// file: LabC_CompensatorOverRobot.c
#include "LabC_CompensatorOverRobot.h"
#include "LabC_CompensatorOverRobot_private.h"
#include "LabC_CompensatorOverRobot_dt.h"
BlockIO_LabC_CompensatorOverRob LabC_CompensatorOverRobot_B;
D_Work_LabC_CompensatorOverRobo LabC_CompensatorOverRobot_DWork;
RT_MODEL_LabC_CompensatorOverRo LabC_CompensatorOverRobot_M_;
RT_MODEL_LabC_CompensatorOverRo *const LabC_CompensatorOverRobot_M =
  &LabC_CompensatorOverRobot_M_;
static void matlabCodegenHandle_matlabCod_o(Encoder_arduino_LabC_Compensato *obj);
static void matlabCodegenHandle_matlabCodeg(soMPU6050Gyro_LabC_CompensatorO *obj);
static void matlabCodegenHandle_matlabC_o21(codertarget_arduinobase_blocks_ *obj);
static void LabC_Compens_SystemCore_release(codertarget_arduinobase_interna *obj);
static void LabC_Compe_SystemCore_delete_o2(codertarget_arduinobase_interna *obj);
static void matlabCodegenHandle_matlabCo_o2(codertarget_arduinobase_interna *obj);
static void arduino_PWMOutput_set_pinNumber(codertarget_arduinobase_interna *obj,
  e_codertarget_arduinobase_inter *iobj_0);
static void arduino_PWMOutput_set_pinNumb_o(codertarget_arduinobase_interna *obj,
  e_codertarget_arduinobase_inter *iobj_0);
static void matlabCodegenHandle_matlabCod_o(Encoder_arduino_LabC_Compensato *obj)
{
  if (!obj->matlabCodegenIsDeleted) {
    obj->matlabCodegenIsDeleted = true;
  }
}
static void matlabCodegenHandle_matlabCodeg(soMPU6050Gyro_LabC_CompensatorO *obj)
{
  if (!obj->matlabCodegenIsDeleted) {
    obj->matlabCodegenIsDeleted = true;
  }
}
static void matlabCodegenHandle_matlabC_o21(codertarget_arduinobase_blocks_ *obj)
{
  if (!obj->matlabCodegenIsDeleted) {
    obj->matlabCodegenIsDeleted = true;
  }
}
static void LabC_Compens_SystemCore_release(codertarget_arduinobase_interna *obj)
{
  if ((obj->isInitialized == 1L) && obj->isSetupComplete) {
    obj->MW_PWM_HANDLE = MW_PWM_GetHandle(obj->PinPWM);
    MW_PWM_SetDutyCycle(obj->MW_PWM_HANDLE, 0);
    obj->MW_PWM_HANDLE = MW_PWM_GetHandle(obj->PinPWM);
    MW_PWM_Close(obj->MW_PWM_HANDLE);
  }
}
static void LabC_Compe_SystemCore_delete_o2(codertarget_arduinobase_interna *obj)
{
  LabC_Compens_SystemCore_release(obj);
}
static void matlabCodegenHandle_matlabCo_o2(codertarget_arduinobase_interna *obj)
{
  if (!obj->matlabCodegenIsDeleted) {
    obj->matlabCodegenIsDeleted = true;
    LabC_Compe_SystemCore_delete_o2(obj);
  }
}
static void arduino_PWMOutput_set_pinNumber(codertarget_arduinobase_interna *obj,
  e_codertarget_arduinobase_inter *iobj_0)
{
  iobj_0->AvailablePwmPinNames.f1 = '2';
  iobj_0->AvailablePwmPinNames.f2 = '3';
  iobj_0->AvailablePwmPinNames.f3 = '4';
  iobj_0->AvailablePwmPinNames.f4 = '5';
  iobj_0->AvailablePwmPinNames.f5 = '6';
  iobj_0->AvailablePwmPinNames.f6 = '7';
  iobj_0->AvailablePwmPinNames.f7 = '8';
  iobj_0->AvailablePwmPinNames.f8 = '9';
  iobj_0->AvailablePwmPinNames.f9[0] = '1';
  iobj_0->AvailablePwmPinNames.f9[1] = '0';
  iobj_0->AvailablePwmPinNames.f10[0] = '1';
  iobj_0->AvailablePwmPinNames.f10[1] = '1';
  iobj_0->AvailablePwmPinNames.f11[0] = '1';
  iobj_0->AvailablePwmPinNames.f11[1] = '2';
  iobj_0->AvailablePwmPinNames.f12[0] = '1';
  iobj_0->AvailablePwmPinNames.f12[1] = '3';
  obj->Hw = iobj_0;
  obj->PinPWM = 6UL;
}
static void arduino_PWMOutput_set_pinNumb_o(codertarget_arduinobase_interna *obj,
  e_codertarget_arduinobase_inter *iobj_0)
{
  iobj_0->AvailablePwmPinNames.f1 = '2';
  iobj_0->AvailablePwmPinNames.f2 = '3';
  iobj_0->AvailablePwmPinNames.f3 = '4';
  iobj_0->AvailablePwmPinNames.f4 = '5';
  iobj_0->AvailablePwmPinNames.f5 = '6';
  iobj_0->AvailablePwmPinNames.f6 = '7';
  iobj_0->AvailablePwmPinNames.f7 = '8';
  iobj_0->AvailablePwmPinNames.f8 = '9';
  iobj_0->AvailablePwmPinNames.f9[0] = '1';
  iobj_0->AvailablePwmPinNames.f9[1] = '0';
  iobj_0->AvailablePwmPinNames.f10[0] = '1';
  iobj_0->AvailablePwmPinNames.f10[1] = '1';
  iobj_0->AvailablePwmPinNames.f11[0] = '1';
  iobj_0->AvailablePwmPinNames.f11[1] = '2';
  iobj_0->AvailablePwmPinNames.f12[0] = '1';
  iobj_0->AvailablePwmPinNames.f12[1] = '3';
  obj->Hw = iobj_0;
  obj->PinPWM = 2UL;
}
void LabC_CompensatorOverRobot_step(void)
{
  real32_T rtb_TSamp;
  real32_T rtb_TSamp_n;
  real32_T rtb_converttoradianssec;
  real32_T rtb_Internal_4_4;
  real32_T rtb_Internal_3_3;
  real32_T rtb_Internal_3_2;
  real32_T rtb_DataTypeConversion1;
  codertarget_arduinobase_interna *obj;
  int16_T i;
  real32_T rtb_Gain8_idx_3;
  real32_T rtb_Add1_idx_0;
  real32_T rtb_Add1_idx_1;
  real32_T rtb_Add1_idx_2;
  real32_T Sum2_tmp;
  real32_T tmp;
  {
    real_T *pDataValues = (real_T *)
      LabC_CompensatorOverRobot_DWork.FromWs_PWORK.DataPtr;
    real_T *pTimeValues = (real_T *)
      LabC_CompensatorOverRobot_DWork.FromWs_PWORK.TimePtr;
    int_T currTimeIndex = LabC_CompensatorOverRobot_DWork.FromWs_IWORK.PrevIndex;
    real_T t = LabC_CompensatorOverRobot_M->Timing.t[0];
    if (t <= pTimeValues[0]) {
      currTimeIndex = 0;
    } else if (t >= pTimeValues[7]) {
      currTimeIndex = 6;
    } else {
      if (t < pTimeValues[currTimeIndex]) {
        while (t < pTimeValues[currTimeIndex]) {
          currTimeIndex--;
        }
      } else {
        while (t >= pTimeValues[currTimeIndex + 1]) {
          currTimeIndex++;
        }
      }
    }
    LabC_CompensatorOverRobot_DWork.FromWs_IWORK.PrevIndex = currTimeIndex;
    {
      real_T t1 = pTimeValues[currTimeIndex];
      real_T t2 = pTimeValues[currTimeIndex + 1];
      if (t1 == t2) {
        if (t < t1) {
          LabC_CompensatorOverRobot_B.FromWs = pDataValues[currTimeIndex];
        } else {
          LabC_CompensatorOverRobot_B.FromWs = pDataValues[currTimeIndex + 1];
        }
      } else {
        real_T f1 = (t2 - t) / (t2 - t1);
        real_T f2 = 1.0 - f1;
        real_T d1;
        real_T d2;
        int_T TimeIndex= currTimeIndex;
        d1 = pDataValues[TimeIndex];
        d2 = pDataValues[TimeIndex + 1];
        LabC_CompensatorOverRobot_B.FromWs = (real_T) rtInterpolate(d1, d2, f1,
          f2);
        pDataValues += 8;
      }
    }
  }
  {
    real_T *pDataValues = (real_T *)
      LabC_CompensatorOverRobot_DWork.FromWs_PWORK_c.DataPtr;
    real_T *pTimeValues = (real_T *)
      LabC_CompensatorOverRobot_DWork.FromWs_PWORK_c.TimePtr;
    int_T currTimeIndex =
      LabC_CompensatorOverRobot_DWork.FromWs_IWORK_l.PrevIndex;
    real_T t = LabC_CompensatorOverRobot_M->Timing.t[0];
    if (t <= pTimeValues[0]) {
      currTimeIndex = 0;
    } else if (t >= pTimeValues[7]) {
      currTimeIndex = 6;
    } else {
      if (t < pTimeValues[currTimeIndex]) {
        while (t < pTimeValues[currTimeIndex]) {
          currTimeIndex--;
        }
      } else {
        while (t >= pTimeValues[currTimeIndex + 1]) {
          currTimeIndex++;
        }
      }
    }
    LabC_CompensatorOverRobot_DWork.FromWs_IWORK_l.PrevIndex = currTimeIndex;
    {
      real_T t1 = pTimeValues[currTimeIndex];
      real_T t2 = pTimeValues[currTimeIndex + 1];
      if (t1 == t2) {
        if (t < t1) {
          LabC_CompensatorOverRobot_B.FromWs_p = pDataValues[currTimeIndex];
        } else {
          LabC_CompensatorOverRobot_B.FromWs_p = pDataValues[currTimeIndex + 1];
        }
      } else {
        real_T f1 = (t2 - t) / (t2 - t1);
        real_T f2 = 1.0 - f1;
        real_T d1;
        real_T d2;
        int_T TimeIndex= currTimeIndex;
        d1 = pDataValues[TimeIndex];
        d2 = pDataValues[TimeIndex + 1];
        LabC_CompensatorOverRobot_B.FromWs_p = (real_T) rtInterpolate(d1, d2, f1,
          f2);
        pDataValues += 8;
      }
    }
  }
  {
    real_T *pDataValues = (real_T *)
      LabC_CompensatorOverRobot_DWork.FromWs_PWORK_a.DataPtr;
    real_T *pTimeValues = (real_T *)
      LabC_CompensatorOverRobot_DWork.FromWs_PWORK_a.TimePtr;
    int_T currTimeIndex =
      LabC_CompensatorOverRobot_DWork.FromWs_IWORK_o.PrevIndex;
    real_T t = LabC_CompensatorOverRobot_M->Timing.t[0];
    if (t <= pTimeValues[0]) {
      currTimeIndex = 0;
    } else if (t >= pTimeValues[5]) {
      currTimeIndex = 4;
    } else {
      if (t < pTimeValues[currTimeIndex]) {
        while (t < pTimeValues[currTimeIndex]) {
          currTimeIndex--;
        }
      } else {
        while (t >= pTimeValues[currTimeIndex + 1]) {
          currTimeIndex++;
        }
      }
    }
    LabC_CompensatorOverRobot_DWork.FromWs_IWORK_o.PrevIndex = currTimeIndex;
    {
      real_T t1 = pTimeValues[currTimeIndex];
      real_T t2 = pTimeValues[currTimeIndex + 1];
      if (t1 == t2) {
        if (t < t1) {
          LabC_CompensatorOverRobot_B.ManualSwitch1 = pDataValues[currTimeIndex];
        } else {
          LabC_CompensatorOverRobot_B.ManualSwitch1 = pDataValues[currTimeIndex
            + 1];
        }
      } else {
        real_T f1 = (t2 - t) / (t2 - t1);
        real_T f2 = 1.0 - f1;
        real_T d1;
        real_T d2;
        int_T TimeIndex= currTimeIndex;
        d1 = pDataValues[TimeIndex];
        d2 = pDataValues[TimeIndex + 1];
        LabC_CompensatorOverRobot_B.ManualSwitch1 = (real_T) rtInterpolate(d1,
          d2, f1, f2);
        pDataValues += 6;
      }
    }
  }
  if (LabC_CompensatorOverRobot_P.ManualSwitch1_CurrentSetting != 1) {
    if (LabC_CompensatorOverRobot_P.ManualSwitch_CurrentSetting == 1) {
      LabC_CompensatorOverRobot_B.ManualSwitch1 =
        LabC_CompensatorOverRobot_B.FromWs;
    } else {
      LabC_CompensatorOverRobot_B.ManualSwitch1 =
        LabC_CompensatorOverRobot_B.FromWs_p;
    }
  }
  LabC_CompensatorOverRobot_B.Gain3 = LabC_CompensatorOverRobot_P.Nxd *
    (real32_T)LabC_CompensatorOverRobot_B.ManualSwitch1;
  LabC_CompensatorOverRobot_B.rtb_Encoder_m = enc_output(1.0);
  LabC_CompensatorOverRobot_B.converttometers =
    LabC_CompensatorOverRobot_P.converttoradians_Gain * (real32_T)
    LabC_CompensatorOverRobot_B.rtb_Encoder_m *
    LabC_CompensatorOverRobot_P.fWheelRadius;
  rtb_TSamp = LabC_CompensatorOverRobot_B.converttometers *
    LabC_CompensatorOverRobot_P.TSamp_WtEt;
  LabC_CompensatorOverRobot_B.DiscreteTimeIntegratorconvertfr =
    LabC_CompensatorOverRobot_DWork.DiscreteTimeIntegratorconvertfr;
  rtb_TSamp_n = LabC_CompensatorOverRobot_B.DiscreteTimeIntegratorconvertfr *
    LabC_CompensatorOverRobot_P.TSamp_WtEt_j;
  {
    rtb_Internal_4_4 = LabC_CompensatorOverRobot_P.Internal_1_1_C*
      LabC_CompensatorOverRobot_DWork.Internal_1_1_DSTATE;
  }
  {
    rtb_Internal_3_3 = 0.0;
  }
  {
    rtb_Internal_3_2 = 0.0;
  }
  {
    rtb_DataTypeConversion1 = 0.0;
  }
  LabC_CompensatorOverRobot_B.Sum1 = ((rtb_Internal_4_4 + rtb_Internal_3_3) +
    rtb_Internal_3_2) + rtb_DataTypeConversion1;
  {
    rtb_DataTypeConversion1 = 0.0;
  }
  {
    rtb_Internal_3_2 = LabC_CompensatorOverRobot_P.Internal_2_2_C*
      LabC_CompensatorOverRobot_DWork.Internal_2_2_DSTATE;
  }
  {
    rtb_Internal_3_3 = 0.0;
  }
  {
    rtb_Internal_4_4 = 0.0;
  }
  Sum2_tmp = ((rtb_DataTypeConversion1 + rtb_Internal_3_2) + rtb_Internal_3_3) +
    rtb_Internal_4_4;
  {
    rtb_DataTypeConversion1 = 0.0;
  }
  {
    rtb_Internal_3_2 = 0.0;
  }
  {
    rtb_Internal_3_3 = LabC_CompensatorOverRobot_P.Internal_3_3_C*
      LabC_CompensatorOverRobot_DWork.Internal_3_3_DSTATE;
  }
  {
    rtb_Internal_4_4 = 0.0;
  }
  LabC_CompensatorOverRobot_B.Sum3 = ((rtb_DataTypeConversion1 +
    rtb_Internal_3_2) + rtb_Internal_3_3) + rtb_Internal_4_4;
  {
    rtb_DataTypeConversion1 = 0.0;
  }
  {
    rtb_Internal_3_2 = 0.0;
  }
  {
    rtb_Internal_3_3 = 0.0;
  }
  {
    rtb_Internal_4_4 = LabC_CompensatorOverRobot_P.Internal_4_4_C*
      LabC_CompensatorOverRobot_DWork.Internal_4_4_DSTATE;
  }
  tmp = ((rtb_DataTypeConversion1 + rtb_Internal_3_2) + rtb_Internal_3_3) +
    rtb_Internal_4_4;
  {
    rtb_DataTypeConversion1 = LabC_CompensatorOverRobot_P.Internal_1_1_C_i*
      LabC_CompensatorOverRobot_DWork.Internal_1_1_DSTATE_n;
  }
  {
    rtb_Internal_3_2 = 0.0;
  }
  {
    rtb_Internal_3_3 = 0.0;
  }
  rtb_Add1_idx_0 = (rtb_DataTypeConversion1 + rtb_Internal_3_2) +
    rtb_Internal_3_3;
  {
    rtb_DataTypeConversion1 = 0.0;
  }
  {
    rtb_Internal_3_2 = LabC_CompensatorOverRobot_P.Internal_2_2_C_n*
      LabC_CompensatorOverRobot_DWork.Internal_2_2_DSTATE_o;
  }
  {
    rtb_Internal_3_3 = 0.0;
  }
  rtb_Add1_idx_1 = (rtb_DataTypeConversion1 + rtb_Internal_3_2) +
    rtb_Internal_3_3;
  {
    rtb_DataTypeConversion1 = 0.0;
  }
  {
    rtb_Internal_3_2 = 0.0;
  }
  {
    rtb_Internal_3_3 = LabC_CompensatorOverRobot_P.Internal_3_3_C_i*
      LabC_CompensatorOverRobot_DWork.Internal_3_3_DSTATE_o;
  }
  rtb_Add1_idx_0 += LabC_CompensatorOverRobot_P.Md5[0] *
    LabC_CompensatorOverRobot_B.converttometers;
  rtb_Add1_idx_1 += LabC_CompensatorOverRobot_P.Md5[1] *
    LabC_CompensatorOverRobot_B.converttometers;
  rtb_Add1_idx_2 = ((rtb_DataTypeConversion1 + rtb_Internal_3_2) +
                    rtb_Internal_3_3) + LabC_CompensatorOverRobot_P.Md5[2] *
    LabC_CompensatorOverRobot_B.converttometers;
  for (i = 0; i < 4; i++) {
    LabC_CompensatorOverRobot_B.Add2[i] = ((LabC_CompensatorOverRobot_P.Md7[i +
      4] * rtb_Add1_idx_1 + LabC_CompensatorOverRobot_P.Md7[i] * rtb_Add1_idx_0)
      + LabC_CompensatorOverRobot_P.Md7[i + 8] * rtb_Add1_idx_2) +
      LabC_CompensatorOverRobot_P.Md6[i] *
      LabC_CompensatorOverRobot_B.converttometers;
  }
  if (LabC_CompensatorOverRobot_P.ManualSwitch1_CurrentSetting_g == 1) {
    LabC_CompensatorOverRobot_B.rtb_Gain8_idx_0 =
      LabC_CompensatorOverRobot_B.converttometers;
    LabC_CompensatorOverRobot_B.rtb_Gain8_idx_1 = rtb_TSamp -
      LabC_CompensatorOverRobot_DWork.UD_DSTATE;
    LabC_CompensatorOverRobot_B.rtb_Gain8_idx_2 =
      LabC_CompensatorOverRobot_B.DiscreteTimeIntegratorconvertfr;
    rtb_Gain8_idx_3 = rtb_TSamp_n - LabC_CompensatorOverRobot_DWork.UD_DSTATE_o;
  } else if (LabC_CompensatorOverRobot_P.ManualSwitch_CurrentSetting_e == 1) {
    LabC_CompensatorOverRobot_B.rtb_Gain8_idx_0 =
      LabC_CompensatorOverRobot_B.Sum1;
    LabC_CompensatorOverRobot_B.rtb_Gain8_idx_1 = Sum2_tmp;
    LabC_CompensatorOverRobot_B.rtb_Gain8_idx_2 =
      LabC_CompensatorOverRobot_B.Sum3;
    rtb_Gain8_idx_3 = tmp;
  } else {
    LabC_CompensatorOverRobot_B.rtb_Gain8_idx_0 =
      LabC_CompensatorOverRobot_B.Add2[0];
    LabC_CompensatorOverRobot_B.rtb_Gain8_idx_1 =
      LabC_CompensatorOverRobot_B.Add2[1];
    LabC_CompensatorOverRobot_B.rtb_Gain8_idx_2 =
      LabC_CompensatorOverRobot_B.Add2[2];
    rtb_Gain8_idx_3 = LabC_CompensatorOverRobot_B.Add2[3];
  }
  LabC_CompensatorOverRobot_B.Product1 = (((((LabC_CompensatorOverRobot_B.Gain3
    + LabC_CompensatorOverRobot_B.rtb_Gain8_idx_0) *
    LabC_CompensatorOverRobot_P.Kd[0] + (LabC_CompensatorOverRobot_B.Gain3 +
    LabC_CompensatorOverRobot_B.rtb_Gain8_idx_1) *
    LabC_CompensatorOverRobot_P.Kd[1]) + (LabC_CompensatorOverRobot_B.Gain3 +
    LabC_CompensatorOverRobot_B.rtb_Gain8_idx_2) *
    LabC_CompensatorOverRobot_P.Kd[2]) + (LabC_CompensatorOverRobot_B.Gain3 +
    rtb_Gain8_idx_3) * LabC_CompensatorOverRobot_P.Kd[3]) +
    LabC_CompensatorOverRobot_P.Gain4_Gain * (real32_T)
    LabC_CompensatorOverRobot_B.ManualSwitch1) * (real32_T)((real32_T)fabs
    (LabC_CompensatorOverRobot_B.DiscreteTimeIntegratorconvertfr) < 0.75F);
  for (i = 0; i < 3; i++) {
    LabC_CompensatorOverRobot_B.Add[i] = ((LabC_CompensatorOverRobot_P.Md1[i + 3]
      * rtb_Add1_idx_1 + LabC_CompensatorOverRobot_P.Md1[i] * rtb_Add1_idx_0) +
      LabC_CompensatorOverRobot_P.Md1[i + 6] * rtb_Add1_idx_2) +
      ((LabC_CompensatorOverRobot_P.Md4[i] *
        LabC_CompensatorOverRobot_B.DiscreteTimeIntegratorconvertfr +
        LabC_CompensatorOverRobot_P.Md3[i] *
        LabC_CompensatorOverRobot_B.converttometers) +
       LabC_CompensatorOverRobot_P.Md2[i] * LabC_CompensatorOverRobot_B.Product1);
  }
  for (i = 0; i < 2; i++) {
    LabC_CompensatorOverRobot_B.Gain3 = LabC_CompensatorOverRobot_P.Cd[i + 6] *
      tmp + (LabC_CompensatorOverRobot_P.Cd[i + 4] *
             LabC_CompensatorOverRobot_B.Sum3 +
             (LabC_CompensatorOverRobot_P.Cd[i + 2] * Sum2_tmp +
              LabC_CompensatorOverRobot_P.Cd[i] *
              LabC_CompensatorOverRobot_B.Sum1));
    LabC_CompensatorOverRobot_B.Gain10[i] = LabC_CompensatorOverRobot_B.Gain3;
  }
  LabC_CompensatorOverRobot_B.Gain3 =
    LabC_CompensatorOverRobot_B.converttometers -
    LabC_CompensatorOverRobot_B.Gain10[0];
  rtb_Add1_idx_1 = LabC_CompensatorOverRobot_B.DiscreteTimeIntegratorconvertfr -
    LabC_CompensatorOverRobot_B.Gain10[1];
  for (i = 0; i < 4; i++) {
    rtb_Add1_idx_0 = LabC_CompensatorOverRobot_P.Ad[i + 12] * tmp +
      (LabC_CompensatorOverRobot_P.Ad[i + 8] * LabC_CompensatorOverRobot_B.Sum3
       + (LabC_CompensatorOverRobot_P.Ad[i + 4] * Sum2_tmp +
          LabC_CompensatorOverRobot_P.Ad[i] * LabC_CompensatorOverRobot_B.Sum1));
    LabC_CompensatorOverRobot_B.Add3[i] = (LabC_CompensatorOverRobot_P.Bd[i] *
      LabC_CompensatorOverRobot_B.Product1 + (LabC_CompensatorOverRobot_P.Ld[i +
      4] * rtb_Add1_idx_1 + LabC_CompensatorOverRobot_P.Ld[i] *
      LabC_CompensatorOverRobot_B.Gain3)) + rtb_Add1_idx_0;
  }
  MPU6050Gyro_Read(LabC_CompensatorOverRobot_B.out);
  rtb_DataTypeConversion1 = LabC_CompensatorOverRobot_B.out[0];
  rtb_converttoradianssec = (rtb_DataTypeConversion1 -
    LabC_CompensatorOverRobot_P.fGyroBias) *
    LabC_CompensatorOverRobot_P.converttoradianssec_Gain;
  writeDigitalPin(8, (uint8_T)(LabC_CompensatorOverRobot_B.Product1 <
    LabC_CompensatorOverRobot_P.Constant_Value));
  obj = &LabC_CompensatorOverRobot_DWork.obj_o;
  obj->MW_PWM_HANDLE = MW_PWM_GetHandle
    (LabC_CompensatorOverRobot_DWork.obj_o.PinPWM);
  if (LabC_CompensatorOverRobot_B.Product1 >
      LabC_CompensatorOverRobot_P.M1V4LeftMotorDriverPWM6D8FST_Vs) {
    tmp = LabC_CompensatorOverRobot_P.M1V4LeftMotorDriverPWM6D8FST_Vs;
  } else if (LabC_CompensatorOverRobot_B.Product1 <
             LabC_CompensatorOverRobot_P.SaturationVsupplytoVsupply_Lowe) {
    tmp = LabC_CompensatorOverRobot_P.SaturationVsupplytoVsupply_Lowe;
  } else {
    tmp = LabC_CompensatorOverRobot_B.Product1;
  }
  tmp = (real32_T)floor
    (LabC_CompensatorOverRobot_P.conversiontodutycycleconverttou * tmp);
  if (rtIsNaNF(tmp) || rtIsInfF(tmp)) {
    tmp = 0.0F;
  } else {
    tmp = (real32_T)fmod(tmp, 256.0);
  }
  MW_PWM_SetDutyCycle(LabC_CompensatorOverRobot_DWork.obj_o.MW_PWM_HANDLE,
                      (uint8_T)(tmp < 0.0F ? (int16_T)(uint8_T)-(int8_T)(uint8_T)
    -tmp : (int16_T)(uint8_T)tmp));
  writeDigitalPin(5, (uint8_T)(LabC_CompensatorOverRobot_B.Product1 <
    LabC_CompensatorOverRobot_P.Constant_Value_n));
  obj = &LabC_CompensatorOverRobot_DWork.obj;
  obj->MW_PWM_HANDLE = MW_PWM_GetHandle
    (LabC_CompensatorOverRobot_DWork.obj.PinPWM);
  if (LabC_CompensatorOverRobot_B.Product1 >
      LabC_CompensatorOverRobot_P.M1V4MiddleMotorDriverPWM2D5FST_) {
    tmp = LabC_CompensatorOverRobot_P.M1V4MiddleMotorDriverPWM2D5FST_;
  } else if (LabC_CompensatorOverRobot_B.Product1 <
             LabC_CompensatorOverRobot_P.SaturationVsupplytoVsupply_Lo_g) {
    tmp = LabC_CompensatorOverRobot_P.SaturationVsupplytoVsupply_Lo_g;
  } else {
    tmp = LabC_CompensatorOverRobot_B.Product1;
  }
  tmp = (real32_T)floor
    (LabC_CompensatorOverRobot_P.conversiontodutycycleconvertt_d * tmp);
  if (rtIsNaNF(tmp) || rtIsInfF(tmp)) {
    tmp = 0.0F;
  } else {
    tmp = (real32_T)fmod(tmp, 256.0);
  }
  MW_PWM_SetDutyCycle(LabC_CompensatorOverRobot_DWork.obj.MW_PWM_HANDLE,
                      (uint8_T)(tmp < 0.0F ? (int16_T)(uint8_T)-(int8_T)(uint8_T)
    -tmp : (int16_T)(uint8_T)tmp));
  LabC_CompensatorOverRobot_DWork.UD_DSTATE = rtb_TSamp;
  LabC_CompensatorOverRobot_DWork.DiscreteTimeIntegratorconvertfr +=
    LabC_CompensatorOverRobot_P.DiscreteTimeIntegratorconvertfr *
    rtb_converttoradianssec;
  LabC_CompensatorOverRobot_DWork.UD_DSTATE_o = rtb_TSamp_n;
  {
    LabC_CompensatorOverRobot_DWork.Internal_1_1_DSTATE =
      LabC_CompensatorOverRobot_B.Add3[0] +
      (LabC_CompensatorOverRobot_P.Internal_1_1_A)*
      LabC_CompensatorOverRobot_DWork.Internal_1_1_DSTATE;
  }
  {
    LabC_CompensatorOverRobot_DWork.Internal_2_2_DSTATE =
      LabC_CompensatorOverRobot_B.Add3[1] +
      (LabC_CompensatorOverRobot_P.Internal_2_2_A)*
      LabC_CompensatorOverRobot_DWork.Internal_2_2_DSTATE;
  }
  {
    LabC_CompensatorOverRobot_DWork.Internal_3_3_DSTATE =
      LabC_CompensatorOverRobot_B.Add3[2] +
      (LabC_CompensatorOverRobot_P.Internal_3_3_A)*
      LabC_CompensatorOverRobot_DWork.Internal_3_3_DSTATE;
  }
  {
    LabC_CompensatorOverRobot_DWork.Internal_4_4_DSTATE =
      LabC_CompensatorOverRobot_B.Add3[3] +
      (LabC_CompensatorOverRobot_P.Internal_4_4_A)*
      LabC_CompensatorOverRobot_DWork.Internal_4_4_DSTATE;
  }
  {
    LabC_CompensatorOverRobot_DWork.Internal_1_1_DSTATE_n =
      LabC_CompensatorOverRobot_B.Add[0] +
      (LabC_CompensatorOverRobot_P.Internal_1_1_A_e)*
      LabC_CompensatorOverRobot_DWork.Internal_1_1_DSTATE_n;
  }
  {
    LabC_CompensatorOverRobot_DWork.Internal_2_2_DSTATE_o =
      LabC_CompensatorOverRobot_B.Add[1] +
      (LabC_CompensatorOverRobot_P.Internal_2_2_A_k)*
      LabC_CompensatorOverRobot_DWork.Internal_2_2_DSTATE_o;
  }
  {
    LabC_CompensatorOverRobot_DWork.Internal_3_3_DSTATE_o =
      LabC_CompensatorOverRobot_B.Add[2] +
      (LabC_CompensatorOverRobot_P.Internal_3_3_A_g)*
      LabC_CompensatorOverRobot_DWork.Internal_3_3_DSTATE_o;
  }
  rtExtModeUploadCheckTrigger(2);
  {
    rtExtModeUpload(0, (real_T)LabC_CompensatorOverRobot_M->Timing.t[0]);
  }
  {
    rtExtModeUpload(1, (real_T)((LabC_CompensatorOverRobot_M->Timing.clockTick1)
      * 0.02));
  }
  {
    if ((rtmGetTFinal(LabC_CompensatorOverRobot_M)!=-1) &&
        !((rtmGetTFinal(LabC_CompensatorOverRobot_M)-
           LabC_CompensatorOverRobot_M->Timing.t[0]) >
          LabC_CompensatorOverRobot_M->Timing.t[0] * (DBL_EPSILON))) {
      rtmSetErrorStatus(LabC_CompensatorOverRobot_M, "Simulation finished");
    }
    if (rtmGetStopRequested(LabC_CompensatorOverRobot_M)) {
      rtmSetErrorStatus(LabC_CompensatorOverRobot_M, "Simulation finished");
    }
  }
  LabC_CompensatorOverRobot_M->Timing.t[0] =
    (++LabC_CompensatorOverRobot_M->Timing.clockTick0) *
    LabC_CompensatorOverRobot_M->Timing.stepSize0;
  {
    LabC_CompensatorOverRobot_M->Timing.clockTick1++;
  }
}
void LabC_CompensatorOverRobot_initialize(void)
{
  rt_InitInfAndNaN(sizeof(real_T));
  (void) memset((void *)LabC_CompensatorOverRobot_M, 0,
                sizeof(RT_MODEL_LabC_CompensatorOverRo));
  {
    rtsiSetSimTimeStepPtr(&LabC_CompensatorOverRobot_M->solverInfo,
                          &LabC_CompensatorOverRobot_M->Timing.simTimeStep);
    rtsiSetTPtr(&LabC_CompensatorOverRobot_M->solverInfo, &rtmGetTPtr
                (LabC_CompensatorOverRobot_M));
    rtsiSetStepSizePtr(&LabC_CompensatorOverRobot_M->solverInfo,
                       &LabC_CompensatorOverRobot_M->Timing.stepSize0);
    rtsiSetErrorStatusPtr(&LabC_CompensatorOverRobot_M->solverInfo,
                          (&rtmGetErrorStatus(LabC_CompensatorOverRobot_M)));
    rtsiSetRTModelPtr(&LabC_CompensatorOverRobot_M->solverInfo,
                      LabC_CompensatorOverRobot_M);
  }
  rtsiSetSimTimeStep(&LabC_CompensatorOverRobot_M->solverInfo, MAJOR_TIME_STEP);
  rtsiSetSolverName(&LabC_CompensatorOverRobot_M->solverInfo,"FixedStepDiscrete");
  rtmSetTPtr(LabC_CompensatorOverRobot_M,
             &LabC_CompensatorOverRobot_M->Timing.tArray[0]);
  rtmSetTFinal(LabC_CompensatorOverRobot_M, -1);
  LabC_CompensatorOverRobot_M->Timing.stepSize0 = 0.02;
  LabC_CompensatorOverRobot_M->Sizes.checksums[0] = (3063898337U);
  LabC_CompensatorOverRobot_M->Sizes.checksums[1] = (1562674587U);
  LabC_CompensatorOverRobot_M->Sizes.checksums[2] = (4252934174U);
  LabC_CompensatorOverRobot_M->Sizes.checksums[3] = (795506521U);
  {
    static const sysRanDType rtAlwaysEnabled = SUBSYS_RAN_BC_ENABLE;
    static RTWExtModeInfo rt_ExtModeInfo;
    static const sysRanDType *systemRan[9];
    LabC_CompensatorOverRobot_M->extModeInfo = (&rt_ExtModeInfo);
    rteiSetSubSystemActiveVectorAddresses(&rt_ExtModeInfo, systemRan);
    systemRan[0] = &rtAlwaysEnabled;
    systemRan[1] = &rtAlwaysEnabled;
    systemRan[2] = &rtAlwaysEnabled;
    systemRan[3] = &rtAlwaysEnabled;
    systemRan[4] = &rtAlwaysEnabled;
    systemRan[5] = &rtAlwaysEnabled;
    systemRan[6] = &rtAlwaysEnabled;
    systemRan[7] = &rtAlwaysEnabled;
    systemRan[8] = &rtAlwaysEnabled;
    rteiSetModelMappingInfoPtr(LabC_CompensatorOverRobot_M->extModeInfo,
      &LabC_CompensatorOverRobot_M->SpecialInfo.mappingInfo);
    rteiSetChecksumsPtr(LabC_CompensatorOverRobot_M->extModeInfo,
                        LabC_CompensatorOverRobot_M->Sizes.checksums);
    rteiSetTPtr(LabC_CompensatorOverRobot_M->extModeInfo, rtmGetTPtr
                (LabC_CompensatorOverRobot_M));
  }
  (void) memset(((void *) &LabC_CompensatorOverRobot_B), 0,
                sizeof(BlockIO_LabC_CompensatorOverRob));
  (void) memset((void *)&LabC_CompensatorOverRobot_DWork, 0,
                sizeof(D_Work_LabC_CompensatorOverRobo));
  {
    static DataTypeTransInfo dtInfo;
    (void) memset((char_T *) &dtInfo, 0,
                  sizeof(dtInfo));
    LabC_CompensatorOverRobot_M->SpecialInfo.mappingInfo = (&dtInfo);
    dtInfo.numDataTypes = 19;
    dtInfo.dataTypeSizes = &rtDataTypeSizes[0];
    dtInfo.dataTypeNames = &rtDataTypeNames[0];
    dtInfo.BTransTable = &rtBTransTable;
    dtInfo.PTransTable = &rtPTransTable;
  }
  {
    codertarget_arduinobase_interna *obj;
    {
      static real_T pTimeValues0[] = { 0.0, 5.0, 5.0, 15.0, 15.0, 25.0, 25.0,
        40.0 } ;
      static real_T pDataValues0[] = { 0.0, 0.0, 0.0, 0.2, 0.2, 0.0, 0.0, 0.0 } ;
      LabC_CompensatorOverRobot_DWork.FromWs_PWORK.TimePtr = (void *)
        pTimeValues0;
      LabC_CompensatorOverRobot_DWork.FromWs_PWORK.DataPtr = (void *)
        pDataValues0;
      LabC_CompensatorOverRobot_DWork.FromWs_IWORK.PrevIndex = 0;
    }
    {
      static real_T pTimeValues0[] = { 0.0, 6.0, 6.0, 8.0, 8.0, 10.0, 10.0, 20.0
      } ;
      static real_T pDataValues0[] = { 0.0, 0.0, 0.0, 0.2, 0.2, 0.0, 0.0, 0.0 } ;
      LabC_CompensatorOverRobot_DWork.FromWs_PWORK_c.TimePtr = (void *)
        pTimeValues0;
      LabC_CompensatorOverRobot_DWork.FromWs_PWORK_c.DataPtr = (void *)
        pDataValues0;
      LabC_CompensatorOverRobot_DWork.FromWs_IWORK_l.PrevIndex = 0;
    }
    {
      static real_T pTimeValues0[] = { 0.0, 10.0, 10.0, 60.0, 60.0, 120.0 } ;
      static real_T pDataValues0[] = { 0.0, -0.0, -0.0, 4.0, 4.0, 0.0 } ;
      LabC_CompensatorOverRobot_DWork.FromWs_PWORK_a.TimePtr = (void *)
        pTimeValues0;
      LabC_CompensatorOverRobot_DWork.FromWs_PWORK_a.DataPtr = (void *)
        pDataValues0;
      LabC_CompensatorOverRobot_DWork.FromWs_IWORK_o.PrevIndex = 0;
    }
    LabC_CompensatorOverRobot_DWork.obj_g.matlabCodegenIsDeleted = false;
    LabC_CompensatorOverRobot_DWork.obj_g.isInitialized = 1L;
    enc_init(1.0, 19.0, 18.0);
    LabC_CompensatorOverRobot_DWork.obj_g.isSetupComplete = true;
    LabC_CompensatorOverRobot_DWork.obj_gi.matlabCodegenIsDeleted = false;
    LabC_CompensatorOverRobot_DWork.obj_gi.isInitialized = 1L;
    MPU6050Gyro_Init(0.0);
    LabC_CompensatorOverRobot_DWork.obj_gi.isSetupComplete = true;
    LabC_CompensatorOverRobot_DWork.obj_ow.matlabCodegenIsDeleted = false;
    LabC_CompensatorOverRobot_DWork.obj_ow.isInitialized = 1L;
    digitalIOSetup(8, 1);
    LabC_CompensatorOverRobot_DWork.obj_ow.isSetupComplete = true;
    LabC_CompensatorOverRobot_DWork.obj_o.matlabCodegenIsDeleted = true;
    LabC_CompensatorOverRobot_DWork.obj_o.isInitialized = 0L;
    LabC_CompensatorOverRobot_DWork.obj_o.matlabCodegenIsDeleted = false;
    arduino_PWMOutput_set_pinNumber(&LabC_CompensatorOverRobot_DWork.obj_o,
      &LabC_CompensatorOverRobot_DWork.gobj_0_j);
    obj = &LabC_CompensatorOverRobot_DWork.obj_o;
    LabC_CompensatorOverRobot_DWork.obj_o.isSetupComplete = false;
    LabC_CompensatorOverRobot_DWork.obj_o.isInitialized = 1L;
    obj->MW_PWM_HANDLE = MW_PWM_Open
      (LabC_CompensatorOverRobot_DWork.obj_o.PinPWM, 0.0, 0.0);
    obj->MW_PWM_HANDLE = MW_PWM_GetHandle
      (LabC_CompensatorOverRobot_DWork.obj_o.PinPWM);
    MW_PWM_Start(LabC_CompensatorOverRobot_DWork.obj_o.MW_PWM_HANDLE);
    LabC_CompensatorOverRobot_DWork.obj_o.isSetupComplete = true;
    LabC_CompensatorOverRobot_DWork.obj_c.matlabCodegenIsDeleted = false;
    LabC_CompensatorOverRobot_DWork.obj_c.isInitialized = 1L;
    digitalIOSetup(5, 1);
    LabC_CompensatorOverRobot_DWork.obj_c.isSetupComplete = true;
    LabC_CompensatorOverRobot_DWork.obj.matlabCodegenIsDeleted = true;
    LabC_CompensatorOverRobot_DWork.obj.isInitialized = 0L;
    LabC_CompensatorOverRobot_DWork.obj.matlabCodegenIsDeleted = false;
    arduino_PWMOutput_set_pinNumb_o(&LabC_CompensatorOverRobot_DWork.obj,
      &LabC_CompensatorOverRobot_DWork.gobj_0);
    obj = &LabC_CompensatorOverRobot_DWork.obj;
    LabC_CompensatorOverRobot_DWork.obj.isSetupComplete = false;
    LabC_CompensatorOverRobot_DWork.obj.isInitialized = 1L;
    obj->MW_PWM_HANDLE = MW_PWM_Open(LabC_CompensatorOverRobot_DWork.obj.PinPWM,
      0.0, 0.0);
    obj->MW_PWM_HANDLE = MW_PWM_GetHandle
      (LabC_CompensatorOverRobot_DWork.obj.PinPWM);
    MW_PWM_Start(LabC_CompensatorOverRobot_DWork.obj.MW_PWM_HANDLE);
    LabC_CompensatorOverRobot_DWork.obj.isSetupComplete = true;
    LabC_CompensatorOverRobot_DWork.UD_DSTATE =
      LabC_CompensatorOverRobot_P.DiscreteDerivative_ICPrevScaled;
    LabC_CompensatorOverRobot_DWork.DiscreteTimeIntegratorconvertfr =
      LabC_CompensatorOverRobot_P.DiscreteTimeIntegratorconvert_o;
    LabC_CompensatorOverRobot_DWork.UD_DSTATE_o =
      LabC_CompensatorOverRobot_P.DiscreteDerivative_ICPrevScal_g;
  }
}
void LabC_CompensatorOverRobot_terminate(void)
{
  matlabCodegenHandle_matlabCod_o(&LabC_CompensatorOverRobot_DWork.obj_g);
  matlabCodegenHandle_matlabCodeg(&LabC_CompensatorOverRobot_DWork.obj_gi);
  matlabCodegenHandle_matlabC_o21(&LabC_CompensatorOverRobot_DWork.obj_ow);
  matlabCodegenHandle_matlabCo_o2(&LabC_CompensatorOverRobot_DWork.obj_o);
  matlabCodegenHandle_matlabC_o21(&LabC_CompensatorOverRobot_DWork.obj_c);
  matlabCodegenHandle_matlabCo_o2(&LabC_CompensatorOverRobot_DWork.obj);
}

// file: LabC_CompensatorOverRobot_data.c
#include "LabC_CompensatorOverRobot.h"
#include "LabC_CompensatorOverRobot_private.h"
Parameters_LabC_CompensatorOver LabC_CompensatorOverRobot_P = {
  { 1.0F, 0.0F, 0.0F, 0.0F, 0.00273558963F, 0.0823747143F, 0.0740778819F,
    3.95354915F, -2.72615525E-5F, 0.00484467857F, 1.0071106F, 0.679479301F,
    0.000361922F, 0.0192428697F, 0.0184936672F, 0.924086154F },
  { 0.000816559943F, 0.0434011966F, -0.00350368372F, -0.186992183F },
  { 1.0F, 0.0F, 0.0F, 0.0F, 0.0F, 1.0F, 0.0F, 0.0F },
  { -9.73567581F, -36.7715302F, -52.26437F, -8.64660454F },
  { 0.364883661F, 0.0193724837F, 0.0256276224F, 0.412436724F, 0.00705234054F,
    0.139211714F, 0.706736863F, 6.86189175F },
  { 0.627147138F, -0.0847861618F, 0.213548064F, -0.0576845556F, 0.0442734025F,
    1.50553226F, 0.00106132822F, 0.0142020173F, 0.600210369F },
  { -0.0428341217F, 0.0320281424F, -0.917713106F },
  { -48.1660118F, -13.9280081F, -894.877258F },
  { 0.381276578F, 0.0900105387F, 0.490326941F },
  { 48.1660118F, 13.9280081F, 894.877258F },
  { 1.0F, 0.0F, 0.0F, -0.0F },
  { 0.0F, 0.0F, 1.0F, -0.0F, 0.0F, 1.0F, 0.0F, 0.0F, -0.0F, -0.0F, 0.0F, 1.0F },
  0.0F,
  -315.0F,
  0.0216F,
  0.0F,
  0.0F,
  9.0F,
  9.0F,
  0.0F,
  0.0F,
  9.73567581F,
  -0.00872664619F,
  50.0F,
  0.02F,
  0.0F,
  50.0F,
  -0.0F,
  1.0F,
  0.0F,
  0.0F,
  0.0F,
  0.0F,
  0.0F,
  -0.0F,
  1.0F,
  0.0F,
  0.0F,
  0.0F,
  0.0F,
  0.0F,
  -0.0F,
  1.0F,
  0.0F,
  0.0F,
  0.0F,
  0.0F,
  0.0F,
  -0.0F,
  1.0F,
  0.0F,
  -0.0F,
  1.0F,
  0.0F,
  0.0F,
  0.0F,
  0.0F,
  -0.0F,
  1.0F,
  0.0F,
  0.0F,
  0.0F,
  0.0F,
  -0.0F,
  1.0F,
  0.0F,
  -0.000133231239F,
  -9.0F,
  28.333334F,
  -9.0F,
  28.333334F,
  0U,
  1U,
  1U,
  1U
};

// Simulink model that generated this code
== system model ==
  M1V4LeftMotorDriverPWM6D8FST : MinSegLibrary_M2V3/M1V4 Left Motor Driver PWM6, D8 FST  <- 1: Product1
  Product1 : Product  <- 1: Sum1, 2: Fcn#1
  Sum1 : Sum  Inputs=++  <- 1: Gain4, 2: Gain#1
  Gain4 : Gain  Gain=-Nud  Multiplication=Matrix(K*u)  <- 1: DataTypeConversion#1
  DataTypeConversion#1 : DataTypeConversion  <- 1: ManualSwitch1
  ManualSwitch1 : ManualSwitch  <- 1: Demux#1, 2: ManualSwitch
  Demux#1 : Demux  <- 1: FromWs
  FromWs : FromWorkspace
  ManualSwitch : ManualSwitch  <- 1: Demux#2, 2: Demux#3
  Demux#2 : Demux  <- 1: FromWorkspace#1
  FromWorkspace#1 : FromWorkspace
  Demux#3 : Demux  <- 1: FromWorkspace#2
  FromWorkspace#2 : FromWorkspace
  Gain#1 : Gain  Gain=Kd  Multiplication=Matrix(K*u)  <- 1: Sum#1
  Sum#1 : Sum  Inputs=++  <- 1: Gain3, 2: ManualSwitch#1
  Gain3 : Gain  Gain=Nxd  Multiplication=Matrix(K*u)  <- 1: DataTypeConversion#1
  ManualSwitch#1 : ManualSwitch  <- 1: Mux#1, 2: ManualSwitch#2
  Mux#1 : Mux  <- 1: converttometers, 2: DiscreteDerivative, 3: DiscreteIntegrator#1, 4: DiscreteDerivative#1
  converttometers : Gain  Gain=fWheelRadius  <- 1: converttoradians
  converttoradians : Gain  Gain=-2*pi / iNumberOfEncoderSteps  <- 1: DataTypeConversion#2
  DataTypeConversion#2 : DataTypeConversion  <- 1: Encoder
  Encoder : MinSegLibrary_M2V3/M2V3 Left Connector 18, 19
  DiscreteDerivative : simulink/Discrete/Discrete Derivative  gainval=1.0  <- 1: converttometers
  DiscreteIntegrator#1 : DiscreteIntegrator  <- 1: converttoradianssec
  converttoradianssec : Gain  Gain=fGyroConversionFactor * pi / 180  <- 1: Sum#2
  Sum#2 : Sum  Inputs=+-  <- 1: DataTypeConversion1, 2: Constant#1
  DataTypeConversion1 : DataTypeConversion  <- 1: MATLABSystem#1
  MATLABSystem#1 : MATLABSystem
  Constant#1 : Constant  Value=fGyroBias
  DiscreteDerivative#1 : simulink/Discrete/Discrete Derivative  gainval=1.0  <- 1: DiscreteIntegrator#1
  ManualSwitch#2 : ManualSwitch  <- 1: LTISystem#1, 2: Add2
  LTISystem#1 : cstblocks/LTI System  <- 1: Add3
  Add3 : Sum  Inputs=+++  <- 1: Gain8, 2: Gain#2, 3: Gain#3
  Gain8 : Gain  Gain=Bd  Multiplication=Matrix(K*u)  <- 1: Product1
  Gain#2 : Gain  Gain=Ld  Multiplication=Matrix(K*u)  <- 1: Sum#3
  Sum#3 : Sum  Inputs=+-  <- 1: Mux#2, 2: Gain10
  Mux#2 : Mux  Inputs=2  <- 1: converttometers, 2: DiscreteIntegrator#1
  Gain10 : Gain  Gain=Cd  Multiplication=Matrix(K*u)  <- 1: LTISystem#1
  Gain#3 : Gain  Gain=Ad  Multiplication=Matrix(K*u)  <- 1: LTISystem#1
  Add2 : Sum  <- 1: Gain#4, 2: Gain#5
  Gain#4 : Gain  Gain=Md6  Multiplication=Matrix(K*u)  <- 1: converttometers
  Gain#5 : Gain  Gain=Md7  Multiplication=Matrix(K*u)  <- 1: Add1
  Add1 : Sum  <- 1: Gain#6, 2: LTISystem#2
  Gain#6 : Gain  Gain=Md5  Multiplication=Matrix(K*u)  <- 1: converttometers
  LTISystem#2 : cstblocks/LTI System  <- 1: Add
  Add : Sum  Inputs=++++  <- 1: Gain#7, 2: Gain#8, 3: Gain#9, 4: Gain
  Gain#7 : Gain  Gain=Md4  Multiplication=Matrix(K*u)  <- 1: DiscreteIntegrator#1
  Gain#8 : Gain  Gain=Md3  Multiplication=Matrix(K*u)  <- 1: converttometers
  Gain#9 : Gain  Gain=Md2  Multiplication=Matrix(K*u)  <- 1: Product1
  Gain : Gain  Gain=Md1  Multiplication=Matrix(K*u)  <- 1: Add1
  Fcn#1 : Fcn  Expr=(abs(u(1))<0.75)  <- 1: DiscreteIntegrator#1
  M1V4MiddleMotorDriverPWM2D5FST : MinSegLibrary_M2V3/M1V4 Middle Motor Driver PWM2, D5 FST  <- 1: Product1
